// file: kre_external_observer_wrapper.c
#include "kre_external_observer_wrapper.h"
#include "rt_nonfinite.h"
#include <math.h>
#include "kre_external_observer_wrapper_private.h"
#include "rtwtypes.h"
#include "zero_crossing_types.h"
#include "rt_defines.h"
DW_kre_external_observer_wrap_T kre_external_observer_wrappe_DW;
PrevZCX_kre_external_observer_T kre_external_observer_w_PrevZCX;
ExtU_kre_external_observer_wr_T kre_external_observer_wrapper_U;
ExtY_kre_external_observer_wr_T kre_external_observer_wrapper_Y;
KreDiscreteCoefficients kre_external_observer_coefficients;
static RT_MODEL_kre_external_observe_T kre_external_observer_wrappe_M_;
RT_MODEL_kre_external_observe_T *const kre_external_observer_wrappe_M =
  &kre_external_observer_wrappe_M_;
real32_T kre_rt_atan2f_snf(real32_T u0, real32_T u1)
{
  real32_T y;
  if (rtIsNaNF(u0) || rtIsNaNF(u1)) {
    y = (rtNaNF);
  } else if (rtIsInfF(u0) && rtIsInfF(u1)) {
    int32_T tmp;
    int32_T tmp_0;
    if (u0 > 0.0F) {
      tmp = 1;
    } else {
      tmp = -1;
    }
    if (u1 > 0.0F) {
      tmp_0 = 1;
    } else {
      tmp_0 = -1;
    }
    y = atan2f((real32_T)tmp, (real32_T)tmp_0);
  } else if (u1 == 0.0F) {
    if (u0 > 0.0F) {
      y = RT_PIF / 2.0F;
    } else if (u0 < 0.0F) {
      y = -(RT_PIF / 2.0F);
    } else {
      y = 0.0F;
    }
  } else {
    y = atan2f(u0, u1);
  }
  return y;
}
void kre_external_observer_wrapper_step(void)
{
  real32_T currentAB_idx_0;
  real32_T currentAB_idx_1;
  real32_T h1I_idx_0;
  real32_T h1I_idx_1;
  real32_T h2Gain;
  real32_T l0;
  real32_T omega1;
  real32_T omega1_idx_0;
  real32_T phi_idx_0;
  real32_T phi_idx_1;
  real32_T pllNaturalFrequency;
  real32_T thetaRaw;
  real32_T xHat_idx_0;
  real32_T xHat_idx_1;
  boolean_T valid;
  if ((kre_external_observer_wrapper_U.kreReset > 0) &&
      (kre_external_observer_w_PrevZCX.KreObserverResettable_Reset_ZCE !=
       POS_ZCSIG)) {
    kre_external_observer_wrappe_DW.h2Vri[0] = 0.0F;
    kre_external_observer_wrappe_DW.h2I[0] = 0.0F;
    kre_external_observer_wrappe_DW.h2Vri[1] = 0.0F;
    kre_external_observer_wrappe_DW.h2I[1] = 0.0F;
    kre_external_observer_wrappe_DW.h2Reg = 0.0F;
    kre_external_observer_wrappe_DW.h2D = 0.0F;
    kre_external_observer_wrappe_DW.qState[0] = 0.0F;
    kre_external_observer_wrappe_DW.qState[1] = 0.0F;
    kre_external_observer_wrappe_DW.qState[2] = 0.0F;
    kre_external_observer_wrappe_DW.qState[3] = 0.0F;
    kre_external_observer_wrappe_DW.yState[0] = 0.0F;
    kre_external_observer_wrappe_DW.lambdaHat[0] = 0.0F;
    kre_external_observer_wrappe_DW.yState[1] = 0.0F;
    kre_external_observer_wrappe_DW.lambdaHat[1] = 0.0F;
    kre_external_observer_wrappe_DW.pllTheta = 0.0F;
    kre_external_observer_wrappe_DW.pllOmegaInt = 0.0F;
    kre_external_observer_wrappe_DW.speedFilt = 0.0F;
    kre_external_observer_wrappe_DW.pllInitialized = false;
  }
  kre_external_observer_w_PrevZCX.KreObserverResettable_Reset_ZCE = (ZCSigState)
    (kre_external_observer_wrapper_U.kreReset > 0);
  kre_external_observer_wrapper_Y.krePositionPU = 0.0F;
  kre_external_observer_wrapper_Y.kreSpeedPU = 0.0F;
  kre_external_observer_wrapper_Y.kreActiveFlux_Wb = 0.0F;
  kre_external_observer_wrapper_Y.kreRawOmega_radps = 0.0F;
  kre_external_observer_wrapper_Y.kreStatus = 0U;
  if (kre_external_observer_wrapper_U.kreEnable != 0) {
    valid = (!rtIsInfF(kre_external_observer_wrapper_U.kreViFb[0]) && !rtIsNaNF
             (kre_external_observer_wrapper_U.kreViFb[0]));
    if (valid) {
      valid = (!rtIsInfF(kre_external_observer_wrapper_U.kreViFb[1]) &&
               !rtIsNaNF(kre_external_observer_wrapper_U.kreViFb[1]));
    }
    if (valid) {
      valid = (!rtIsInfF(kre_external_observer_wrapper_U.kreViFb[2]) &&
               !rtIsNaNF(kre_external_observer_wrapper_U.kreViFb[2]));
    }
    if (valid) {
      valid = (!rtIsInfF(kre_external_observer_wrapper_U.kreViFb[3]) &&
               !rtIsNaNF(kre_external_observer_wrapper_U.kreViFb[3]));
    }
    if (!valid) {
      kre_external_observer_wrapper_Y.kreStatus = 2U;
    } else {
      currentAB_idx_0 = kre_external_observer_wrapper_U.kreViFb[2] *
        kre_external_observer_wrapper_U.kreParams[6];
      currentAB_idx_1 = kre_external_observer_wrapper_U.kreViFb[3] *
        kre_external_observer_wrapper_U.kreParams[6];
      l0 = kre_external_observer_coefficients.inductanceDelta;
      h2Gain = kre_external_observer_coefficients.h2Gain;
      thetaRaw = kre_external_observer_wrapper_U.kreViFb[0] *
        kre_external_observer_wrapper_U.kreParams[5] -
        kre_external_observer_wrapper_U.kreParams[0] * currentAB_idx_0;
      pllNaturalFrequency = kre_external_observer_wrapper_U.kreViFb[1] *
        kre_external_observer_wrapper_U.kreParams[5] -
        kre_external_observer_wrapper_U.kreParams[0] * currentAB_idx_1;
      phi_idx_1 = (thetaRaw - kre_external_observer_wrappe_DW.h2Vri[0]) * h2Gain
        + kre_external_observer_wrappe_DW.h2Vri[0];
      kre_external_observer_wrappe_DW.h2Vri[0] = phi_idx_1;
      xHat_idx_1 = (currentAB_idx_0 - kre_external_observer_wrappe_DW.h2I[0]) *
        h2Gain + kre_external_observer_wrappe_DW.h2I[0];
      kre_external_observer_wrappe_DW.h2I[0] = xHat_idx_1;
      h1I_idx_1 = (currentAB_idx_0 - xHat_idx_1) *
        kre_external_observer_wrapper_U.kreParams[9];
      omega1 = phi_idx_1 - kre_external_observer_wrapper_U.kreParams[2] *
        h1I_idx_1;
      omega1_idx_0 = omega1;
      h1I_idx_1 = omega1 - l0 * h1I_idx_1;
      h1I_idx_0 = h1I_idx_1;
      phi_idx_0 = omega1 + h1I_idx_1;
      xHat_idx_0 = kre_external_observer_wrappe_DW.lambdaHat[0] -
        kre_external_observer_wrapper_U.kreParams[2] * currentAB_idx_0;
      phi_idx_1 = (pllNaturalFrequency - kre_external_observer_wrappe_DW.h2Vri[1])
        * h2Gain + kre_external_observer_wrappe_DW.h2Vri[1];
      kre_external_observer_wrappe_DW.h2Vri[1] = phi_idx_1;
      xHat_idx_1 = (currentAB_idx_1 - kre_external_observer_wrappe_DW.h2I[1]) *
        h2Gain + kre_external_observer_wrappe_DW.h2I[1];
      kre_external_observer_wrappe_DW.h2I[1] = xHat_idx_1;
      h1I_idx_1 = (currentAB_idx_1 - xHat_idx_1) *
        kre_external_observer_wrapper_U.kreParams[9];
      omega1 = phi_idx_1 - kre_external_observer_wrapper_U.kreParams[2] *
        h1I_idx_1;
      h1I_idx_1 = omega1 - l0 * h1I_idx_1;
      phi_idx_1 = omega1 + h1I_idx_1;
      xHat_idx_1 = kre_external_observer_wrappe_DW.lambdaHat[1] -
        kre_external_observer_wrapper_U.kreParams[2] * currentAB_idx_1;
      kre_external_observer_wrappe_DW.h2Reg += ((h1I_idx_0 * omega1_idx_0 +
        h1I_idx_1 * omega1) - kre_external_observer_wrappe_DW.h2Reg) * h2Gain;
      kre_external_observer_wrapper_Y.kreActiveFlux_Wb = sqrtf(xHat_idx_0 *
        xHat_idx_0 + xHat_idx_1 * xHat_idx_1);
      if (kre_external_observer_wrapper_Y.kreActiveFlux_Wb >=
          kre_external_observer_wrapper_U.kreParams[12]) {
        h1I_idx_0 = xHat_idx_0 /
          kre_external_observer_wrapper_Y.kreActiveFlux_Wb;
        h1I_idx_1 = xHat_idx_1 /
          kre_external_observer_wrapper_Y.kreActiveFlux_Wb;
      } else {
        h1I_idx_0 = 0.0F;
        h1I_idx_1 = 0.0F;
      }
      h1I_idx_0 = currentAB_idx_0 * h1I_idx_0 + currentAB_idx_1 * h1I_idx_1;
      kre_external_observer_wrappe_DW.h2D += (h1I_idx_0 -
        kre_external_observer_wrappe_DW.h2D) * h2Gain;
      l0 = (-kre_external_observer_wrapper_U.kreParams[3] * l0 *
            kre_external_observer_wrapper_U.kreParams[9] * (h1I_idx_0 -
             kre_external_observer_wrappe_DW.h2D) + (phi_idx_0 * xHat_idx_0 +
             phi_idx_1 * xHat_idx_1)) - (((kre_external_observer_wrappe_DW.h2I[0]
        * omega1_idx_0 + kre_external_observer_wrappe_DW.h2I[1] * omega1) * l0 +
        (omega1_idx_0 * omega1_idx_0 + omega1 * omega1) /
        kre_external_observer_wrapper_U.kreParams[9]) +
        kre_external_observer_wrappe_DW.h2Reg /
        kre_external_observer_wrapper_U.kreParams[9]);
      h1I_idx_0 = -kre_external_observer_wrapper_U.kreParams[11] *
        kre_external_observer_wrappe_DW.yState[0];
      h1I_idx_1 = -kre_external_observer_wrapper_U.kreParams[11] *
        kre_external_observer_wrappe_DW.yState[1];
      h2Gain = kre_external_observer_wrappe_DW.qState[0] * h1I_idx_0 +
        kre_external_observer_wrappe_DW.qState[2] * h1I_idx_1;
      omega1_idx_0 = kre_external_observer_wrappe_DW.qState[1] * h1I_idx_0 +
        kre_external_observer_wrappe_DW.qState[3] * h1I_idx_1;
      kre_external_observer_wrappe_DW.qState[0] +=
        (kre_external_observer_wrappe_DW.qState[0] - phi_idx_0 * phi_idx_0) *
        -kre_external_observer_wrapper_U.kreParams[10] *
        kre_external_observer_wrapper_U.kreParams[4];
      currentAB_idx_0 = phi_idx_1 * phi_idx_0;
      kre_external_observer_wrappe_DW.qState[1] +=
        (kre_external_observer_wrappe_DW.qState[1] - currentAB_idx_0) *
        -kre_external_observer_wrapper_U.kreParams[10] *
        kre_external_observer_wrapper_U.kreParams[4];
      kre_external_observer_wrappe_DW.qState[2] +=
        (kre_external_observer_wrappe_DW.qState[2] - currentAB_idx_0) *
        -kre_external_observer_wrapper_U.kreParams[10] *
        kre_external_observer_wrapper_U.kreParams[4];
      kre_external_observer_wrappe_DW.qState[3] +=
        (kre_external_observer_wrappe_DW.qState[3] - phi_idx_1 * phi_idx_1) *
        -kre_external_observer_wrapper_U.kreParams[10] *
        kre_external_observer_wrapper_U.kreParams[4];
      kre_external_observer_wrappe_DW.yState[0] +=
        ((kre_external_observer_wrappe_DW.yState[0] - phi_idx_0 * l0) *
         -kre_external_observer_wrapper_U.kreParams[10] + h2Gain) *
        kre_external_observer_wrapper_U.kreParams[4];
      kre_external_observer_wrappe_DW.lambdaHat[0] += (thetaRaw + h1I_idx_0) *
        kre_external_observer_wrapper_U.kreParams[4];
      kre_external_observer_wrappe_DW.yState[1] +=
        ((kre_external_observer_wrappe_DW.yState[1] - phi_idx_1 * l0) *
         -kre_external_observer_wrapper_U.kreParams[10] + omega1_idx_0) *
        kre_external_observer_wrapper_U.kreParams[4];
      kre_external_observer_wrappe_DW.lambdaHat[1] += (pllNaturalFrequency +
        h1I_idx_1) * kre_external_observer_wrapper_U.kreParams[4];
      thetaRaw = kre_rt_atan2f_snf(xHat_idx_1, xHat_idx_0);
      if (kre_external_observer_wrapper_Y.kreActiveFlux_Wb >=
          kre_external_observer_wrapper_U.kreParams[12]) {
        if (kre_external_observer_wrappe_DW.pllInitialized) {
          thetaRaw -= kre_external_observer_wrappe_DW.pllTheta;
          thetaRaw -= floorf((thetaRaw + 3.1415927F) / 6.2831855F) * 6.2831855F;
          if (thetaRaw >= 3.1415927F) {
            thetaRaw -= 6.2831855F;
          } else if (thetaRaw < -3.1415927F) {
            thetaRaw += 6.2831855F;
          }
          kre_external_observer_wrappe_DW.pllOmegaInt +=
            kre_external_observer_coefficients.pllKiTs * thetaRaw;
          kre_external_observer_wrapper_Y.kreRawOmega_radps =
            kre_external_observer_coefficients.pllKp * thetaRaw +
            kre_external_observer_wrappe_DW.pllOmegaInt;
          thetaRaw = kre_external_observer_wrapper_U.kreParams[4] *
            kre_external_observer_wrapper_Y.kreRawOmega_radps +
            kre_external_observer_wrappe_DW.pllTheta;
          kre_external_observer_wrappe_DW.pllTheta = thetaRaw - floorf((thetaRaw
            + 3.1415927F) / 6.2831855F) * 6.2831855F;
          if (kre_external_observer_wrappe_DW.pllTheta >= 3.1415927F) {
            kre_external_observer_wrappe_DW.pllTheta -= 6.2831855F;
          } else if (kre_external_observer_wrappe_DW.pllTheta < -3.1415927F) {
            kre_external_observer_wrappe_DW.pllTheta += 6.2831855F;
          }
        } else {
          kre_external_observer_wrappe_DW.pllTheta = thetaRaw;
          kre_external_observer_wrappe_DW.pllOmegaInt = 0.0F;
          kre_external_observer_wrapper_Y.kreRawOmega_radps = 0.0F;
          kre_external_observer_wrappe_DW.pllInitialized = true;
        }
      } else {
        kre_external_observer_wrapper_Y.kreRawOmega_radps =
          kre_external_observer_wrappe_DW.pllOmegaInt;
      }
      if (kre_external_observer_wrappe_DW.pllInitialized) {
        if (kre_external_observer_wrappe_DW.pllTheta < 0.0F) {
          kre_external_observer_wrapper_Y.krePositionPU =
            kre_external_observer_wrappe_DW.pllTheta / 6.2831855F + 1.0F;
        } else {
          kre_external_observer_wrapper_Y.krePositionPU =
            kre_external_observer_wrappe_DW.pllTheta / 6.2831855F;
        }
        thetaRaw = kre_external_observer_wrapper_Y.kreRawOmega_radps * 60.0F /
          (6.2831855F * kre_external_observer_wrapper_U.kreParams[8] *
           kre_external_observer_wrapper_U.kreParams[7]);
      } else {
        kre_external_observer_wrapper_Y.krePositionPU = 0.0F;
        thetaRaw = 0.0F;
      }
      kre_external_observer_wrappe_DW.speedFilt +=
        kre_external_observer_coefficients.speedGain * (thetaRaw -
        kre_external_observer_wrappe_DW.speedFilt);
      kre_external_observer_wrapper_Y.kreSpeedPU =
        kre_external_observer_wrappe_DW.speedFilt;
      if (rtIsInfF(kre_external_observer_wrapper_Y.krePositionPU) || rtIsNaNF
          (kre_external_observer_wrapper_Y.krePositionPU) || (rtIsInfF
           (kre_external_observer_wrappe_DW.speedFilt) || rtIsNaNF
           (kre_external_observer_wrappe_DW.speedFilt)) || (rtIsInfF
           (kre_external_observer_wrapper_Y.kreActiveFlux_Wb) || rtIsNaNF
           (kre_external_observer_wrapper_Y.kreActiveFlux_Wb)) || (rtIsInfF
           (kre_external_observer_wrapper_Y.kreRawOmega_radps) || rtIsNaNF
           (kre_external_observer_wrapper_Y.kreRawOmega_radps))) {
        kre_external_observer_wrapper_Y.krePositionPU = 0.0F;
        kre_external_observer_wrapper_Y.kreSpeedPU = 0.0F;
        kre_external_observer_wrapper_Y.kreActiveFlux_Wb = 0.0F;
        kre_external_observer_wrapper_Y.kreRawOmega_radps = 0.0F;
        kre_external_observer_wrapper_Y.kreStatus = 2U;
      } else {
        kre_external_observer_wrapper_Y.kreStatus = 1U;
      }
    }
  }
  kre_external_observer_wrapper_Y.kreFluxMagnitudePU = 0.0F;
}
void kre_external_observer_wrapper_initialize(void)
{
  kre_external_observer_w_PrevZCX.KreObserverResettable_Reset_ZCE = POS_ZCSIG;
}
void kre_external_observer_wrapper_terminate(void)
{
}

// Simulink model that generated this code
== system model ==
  kreEnable : Inport
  kreViFb : Inport
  kreParams : Inport
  kreReset : Inport
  Inport#1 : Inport
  krePositionPU : Outport  <- 1: KreObserverResettable
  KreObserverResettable : Subsystem  <- 1: kreEnable, 2: kreViFb, 3: kreParams, 4: Inport#1, Reset: kreReset
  kreSpeedPU : Outport  <- 1: KreObserverResettable/2
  kreFluxMagnitudePU : Outport  <- 1: KreObserverResettable/3
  kreStatus : Outport  <- 1: KreObserverResettable/4
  kreActiveFlux_Wb : Outport  <- 1: KreObserverResettable/5
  kreRawOmega_radps : Outport  <- 1: KreObserverResettable/6
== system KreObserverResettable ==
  Inport#2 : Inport
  Inport#3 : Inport
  Inport#4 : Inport
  Inport#5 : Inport
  Reset : ResetPort
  Outport#1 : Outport  <- 1: MATLABFunction#1
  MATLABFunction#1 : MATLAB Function  <- 1: Inport#2, 2: Inport#3, 3: Inport#4, 4: Inport#5
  Outport#2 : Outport  <- 1: MATLABFunction#1/2
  Outport#3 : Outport  <- 1: MATLABFunction#1/3
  Outport#4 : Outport  <- 1: MATLABFunction#1/4
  Outport#5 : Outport  <- 1: MATLABFunction#1/5
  Outport#6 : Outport  <- 1: MATLABFunction#1/6
== matlab function MATLABFunction#1 ==
function [krePositionPU, kreSpeedPU, kreFluxMagnitudePU, kreStatus, kreActiveFlux_Wb, kreRawOmega_radps] = fcn(kreEnable, kreViFb, kreParams, krePllParams)
%#codegen
[krePositionPU, kreSpeedPU, kreFluxMagnitudePU, kreActiveFlux_Wb, kreRawOmega_radps, kreStatus] = kre_external_observer_diagnostic_step(kreEnable, kreViFb, kreParams, krePllParams);
end
